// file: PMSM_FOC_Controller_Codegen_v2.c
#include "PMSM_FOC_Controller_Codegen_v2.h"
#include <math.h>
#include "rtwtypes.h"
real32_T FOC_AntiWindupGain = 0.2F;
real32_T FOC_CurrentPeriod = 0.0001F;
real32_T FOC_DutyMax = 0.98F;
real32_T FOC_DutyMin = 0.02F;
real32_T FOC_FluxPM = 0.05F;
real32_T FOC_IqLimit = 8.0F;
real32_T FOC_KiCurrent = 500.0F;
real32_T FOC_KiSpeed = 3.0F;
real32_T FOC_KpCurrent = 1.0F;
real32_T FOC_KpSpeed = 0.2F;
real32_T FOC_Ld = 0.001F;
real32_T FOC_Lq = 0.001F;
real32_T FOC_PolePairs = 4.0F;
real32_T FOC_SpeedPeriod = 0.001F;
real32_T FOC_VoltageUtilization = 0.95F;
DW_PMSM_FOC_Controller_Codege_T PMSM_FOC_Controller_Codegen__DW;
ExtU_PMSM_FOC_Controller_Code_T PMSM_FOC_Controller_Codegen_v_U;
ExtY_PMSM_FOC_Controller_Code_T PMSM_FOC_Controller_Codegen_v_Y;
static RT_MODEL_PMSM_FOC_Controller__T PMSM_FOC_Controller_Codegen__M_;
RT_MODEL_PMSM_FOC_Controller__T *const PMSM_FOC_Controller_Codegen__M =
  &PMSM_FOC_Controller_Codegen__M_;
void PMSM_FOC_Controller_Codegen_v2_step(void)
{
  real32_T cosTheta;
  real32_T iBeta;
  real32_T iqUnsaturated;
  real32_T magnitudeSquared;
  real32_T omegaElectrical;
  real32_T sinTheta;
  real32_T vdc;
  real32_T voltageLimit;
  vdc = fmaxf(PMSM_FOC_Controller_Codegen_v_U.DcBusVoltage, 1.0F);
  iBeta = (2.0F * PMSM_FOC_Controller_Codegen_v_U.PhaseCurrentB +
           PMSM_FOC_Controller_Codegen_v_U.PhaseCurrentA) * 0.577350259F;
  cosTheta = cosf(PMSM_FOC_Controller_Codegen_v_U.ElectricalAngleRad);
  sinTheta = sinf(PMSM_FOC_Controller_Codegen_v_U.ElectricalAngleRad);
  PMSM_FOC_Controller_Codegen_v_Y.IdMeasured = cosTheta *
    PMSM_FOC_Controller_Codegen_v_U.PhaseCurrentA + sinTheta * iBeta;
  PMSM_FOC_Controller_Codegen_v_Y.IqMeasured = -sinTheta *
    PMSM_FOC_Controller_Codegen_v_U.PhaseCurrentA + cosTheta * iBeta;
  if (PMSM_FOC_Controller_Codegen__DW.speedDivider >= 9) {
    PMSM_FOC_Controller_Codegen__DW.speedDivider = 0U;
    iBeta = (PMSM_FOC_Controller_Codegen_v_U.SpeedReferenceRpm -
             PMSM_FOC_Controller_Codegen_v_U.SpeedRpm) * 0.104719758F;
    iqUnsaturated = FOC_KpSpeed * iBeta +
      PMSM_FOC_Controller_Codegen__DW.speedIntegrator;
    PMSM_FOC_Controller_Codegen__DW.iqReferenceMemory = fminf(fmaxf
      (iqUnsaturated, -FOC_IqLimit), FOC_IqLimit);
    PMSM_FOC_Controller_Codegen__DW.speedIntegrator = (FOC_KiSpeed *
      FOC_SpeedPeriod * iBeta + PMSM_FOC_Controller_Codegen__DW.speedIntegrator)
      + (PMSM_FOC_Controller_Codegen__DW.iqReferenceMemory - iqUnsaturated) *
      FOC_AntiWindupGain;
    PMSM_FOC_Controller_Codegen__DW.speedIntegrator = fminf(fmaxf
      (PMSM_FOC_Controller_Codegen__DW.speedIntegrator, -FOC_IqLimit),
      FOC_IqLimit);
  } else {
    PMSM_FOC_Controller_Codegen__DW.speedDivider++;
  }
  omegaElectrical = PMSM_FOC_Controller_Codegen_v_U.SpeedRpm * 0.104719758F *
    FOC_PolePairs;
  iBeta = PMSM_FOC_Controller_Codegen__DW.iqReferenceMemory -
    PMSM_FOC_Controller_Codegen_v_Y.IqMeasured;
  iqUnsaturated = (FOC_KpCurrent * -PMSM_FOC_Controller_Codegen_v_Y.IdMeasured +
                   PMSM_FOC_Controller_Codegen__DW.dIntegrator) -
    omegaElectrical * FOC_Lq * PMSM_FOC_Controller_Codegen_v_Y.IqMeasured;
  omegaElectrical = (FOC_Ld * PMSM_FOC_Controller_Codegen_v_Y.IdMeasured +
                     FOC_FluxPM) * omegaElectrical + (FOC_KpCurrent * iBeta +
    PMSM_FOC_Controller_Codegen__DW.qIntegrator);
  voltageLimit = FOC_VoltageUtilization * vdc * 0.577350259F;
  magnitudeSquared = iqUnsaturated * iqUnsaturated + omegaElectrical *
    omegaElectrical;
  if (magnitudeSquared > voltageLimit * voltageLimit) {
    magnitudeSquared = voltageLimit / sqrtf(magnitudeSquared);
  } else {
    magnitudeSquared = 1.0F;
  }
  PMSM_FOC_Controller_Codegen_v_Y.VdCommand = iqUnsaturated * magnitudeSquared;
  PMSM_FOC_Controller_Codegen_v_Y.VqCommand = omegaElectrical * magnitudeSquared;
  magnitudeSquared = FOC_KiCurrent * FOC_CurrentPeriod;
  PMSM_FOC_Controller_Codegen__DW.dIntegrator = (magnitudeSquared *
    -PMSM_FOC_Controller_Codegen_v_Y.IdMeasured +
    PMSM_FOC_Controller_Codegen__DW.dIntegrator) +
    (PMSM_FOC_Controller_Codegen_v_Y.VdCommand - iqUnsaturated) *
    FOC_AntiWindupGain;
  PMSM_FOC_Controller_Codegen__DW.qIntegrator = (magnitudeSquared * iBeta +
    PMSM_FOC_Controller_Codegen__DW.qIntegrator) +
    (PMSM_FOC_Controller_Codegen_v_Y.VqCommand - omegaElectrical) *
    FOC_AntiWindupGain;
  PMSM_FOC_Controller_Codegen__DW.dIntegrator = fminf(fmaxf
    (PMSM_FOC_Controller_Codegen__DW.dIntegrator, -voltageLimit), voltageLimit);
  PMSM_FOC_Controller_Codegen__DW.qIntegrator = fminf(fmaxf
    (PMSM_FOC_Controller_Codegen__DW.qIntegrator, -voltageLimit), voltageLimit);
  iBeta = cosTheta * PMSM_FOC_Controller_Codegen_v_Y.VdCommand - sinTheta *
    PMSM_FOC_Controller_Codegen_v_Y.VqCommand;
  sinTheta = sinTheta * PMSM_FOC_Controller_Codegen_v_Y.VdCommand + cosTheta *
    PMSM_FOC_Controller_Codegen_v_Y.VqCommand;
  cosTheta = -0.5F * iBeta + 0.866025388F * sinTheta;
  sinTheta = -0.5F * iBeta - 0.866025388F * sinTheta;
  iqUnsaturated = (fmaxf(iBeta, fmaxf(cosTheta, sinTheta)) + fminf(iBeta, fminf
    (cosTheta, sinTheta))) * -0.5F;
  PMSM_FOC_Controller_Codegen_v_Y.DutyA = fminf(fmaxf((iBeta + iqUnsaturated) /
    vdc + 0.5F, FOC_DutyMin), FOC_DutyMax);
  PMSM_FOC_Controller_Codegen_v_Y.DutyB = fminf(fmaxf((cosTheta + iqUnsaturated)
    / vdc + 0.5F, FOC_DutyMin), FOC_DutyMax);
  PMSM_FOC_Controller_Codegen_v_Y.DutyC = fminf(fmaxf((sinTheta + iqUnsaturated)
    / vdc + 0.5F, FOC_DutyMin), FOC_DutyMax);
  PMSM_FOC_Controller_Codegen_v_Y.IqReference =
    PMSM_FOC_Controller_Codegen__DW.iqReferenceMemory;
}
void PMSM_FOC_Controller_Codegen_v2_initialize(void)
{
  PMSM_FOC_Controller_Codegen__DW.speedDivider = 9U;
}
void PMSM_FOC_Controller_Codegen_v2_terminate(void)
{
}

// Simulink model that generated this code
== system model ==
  SpeedReferenceRpm : Inport
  SpeedRpm : Inport
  PhaseCurrentA : Inport
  PhaseCurrentB : Inport
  ElectricalAngleRad : Inport
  DcBusVoltage : Inport
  DutyA : Outport  <- 1: MATLABFunction#1
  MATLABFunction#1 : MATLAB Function  <- 1: SpeedReferenceRpm, 2: SpeedRpm, 3: PhaseCurrentA, 4: PhaseCurrentB, 5: ElectricalAngleRad, 6: DcBusVoltage
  DutyB : Outport  <- 1: MATLABFunction#1/2
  DutyC : Outport  <- 1: MATLABFunction#1/3
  IqReference : Outport  <- 1: MATLABFunction#1/4
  IdMeasured : Outport  <- 1: MATLABFunction#1/5
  IqMeasured : Outport  <- 1: MATLABFunction#1/6
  VdCommand : Outport  <- 1: MATLABFunction#1/7
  VqCommand : Outport  <- 1: MATLABFunction#1/8
== matlab function MATLABFunction#1 ==
function [dutyA, dutyB, dutyC, iqReference, idMeasured, iqMeasured, vdCommand, vqCommand] = ...
    foc_controller_codegen_core(speedReferenceRpm, speedRpm, ia, ib, thetaElectrical, vdc, FOC_CurrentPeriod, FOC_SpeedPeriod, FOC_PolePairs, FOC_Ld, FOC_Lq, FOC_FluxPM, FOC_KpCurrent, FOC_KiCurrent, FOC_KpSpeed, FOC_KiSpeed, FOC_IqLimit, FOC_VoltageUtilization, FOC_AntiWindupGain, FOC_DutyMin, FOC_DutyMax)
%#codegen
% Code-generation implementation of the basic PMSM FOC controller.

% These states belong to the deployable controller. The generated
% initialize function resets them when the application starts.
persistent speedIntegrator dIntegrator qIntegrator iqReferenceMemory speedDivider
if isempty(speedIntegrator)
    speedIntegrator = single(0.0);
    dIntegrator = single(0.0);
    qIntegrator = single(0.0);
    iqReferenceMemory = single(0.0);
    speedDivider = uint8(9); % Execute the 1 ms speed loop on the first call.
end

vdc = max(vdc, single(1.0));
sqrtThree = single(1.7320508075688772);
inverseSqrtThree = single(0.5773502691896258);
rpmToRadians = single(0.1047197551196598);

% Clarke and Park transforms.
iAlpha = ia;
iBeta = (ia + single(2.0) * ib) * inverseSqrtThree;
cosTheta = cos(thetaElectrical);
sinTheta = sin(thetaElectrical);
idMeasured = cosTheta * iAlpha + sinTheta * iBeta;
iqMeasured = -sinTheta * iAlpha + cosTheta * iBeta;

% The controller step runs at 100 us; execute the speed PI every ten calls.
if speedDivider >= uint8(9)
    speedDivider = uint8(0);
    speedError = (speedReferenceRpm - speedRpm) * rpmToRadians;
    iqUnsaturated = FOC_KpSpeed * speedError + speedIntegrator;
    iqReference = min(max(iqUnsaturated, -FOC_IqLimit), FOC_IqLimit);
    speedIntegrator = speedIntegrator + ...
        FOC_KiSpeed * FOC_SpeedPeriod * speedError + ...
        FOC_AntiWindupGain * (iqReference - iqUnsaturated);
    speedIntegrator = min(max(speedIntegrator, -FOC_IqLimit), FOC_IqLimit);
else
    speedDivider = speedDivider + uint8(1);
    iqReference = iqReferenceMemory;
end
iqReferenceMemory = iqReference;

% Current PI, dq decoupling and back-EMF feed-forward.
omegaElectrical = speedRpm * rpmToRadians * FOC_PolePairs;
dError = -idMeasured;
qError = iqReference - iqMeasured;
vdRaw = FOC_KpCurrent * dError + dIntegrator - ...
    omegaElectrical * FOC_Lq * iqMeasured;
vqRaw = FOC_KpCurrent * qError + qIntegrator + ...
    omegaElectrical * (FOC_Ld * idMeasured + FOC_FluxPM);

voltageLimit = FOC_VoltageUtilization * vdc * inverseSqrtThree;
magnitudeSquared = vdRaw * vdRaw + vqRaw * vqRaw;
if magnitudeSquared > voltageLimit * voltageLimit
    voltageScale = voltageLimit / sqrt(magnitudeSquared);
else
    voltageScale = single(1.0);
end
vdCommand = vdRaw * voltageScale;
vqCommand = vqRaw * voltageScale;

dIntegrator = dIntegrator + FOC_KiCurrent * FOC_CurrentPeriod * dError + ...
    FOC_AntiWindupGain * (vdCommand - vdRaw);
qIntegrator = qIntegrator + FOC_KiCurrent * FOC_CurrentPeriod * qError + ...
    FOC_AntiWindupGain * (vqCommand - vqRaw);
dIntegrator = min(max(dIntegrator, -voltageLimit), voltageLimit);
qIntegrator = min(max(qIntegrator, -voltageLimit), voltageLimit);

% Inverse Park and centered SVPWM duty ratios.
vAlpha = cosTheta * vdCommand - sinTheta * vqCommand;
vBeta = sinTheta * vdCommand + cosTheta * vqCommand;
va = vAlpha;
vb = single(-0.5) * vAlpha + single(0.5) * sqrtThree * vBeta;
vc = single(-0.5) * vAlpha - single(0.5) * sqrtThree * vBeta;
maximumPhase = max(va, max(vb, vc));
minimumPhase = min(va, min(vb, vc));
commonMode = single(-0.5) * (maximumPhase + minimumPhase);
dutyA = single(0.5) + (va + commonMode) / vdc;
dutyB = single(0.5) + (vb + commonMode) / vdc;
dutyC = single(0.5) + (vc + commonMode) / vdc;
dutyA = min(max(dutyA, FOC_DutyMin), FOC_DutyMax);
dutyB = min(max(dutyB, FOC_DutyMin), FOC_DutyMax);
dutyC = min(max(dutyC, FOC_DutyMin), FOC_DutyMax);
end
